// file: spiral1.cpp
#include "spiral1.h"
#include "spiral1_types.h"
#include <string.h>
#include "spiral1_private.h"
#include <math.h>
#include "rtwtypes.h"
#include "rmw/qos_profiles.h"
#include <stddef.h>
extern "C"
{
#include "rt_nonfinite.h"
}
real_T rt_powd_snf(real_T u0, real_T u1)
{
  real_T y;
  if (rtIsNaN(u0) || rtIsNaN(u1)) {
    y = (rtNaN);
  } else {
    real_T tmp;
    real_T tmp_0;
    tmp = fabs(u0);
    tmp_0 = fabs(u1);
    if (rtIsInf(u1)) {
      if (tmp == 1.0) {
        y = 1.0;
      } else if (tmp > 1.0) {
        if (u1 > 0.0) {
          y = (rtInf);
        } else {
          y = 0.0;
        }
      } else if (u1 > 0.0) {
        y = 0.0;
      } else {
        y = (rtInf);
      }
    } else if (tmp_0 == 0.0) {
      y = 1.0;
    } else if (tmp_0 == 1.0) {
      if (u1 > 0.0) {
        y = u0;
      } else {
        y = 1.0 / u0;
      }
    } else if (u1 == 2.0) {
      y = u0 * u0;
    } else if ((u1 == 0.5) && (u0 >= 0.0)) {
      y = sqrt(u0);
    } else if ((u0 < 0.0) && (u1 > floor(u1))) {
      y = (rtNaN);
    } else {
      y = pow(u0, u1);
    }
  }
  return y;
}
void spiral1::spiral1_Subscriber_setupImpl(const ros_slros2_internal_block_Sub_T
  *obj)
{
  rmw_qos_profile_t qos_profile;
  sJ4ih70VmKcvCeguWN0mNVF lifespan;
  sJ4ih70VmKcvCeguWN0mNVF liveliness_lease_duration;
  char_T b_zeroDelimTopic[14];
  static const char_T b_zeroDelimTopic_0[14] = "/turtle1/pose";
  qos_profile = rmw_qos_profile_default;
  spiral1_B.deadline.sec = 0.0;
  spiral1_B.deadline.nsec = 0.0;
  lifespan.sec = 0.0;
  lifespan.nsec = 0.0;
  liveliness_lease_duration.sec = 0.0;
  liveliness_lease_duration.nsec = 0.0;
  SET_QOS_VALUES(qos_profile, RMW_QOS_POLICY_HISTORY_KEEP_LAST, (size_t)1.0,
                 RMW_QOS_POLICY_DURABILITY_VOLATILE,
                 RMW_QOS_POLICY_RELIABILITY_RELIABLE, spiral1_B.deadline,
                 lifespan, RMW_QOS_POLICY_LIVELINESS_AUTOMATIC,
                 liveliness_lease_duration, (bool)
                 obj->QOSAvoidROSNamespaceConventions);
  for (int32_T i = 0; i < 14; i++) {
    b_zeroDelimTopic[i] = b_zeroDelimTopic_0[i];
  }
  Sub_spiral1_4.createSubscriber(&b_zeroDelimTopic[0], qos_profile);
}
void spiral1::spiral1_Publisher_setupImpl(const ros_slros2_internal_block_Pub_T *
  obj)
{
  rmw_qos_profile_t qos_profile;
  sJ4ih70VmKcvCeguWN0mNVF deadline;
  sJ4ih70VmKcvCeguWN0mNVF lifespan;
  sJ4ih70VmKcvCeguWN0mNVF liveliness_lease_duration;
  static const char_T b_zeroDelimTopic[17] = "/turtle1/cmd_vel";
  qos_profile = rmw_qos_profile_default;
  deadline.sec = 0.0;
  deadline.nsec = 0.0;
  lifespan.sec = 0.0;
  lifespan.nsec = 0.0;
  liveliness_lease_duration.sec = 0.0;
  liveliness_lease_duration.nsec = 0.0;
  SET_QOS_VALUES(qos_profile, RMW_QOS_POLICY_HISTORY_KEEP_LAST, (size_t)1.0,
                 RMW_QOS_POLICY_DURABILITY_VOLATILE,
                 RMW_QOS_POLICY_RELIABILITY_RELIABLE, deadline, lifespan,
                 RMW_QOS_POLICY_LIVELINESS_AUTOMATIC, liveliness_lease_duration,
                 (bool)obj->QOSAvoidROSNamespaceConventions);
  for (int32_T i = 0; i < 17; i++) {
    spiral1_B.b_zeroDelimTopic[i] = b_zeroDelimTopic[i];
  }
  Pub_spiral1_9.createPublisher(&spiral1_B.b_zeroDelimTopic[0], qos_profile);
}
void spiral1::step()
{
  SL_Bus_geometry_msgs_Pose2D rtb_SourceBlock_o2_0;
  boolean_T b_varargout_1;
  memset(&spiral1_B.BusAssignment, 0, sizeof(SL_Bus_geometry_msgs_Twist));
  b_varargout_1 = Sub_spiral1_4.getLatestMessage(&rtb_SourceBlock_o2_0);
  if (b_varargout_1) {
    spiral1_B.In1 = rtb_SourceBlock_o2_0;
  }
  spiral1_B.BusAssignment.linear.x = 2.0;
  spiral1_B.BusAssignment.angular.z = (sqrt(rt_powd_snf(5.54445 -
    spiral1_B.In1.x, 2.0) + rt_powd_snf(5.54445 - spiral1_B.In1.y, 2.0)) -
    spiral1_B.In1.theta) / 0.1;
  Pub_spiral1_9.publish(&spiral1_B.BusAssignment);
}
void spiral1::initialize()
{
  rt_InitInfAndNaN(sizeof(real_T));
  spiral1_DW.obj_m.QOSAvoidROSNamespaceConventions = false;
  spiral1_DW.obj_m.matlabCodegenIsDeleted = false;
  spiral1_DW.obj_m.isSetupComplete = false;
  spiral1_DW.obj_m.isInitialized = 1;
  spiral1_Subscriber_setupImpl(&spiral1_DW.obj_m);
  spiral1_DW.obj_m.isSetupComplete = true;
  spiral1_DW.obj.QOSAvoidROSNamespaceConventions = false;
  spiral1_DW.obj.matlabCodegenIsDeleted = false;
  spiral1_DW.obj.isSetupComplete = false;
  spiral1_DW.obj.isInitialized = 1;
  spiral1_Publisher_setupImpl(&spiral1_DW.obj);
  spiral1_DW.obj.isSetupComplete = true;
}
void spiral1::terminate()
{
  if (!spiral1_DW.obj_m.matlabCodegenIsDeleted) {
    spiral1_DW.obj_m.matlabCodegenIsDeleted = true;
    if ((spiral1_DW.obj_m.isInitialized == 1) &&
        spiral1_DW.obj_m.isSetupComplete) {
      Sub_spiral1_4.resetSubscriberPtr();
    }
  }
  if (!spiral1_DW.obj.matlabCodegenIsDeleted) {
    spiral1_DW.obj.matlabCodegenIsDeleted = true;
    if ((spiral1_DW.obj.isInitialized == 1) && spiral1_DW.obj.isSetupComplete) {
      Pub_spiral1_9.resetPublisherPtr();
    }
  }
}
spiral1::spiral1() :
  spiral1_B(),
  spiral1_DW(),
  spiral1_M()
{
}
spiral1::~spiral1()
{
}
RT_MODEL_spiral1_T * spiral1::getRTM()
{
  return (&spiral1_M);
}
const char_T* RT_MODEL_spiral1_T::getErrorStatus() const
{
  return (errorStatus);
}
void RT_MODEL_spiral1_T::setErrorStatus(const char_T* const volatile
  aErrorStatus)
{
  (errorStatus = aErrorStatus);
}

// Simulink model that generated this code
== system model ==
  Publish#1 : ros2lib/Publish  <- 1: BusAssignment
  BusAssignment : BusAssignment  <- 1: BlankMessage#1, 2: Constant#1, 3: Product#1
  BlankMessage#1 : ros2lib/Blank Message
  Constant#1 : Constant  Value=2
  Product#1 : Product  Inputs=*/  <- 1: Sum#1, 2: Constant#2
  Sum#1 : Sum  Inputs=+-  <- 1: Fcn#1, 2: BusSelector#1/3
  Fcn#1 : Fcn  Expr=sqrt(u(1)^2+u(2)^2)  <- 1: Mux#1
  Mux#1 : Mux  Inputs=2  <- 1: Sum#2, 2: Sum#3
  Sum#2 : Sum  Inputs=+-  <- 1: Constant#3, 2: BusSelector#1
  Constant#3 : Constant  Value=5.54445
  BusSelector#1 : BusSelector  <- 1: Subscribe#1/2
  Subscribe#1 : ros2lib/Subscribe
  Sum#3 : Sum  Inputs=+-  <- 1: Constant#4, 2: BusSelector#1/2
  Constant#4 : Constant  Value=5.54445
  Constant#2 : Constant  Value=0.1
